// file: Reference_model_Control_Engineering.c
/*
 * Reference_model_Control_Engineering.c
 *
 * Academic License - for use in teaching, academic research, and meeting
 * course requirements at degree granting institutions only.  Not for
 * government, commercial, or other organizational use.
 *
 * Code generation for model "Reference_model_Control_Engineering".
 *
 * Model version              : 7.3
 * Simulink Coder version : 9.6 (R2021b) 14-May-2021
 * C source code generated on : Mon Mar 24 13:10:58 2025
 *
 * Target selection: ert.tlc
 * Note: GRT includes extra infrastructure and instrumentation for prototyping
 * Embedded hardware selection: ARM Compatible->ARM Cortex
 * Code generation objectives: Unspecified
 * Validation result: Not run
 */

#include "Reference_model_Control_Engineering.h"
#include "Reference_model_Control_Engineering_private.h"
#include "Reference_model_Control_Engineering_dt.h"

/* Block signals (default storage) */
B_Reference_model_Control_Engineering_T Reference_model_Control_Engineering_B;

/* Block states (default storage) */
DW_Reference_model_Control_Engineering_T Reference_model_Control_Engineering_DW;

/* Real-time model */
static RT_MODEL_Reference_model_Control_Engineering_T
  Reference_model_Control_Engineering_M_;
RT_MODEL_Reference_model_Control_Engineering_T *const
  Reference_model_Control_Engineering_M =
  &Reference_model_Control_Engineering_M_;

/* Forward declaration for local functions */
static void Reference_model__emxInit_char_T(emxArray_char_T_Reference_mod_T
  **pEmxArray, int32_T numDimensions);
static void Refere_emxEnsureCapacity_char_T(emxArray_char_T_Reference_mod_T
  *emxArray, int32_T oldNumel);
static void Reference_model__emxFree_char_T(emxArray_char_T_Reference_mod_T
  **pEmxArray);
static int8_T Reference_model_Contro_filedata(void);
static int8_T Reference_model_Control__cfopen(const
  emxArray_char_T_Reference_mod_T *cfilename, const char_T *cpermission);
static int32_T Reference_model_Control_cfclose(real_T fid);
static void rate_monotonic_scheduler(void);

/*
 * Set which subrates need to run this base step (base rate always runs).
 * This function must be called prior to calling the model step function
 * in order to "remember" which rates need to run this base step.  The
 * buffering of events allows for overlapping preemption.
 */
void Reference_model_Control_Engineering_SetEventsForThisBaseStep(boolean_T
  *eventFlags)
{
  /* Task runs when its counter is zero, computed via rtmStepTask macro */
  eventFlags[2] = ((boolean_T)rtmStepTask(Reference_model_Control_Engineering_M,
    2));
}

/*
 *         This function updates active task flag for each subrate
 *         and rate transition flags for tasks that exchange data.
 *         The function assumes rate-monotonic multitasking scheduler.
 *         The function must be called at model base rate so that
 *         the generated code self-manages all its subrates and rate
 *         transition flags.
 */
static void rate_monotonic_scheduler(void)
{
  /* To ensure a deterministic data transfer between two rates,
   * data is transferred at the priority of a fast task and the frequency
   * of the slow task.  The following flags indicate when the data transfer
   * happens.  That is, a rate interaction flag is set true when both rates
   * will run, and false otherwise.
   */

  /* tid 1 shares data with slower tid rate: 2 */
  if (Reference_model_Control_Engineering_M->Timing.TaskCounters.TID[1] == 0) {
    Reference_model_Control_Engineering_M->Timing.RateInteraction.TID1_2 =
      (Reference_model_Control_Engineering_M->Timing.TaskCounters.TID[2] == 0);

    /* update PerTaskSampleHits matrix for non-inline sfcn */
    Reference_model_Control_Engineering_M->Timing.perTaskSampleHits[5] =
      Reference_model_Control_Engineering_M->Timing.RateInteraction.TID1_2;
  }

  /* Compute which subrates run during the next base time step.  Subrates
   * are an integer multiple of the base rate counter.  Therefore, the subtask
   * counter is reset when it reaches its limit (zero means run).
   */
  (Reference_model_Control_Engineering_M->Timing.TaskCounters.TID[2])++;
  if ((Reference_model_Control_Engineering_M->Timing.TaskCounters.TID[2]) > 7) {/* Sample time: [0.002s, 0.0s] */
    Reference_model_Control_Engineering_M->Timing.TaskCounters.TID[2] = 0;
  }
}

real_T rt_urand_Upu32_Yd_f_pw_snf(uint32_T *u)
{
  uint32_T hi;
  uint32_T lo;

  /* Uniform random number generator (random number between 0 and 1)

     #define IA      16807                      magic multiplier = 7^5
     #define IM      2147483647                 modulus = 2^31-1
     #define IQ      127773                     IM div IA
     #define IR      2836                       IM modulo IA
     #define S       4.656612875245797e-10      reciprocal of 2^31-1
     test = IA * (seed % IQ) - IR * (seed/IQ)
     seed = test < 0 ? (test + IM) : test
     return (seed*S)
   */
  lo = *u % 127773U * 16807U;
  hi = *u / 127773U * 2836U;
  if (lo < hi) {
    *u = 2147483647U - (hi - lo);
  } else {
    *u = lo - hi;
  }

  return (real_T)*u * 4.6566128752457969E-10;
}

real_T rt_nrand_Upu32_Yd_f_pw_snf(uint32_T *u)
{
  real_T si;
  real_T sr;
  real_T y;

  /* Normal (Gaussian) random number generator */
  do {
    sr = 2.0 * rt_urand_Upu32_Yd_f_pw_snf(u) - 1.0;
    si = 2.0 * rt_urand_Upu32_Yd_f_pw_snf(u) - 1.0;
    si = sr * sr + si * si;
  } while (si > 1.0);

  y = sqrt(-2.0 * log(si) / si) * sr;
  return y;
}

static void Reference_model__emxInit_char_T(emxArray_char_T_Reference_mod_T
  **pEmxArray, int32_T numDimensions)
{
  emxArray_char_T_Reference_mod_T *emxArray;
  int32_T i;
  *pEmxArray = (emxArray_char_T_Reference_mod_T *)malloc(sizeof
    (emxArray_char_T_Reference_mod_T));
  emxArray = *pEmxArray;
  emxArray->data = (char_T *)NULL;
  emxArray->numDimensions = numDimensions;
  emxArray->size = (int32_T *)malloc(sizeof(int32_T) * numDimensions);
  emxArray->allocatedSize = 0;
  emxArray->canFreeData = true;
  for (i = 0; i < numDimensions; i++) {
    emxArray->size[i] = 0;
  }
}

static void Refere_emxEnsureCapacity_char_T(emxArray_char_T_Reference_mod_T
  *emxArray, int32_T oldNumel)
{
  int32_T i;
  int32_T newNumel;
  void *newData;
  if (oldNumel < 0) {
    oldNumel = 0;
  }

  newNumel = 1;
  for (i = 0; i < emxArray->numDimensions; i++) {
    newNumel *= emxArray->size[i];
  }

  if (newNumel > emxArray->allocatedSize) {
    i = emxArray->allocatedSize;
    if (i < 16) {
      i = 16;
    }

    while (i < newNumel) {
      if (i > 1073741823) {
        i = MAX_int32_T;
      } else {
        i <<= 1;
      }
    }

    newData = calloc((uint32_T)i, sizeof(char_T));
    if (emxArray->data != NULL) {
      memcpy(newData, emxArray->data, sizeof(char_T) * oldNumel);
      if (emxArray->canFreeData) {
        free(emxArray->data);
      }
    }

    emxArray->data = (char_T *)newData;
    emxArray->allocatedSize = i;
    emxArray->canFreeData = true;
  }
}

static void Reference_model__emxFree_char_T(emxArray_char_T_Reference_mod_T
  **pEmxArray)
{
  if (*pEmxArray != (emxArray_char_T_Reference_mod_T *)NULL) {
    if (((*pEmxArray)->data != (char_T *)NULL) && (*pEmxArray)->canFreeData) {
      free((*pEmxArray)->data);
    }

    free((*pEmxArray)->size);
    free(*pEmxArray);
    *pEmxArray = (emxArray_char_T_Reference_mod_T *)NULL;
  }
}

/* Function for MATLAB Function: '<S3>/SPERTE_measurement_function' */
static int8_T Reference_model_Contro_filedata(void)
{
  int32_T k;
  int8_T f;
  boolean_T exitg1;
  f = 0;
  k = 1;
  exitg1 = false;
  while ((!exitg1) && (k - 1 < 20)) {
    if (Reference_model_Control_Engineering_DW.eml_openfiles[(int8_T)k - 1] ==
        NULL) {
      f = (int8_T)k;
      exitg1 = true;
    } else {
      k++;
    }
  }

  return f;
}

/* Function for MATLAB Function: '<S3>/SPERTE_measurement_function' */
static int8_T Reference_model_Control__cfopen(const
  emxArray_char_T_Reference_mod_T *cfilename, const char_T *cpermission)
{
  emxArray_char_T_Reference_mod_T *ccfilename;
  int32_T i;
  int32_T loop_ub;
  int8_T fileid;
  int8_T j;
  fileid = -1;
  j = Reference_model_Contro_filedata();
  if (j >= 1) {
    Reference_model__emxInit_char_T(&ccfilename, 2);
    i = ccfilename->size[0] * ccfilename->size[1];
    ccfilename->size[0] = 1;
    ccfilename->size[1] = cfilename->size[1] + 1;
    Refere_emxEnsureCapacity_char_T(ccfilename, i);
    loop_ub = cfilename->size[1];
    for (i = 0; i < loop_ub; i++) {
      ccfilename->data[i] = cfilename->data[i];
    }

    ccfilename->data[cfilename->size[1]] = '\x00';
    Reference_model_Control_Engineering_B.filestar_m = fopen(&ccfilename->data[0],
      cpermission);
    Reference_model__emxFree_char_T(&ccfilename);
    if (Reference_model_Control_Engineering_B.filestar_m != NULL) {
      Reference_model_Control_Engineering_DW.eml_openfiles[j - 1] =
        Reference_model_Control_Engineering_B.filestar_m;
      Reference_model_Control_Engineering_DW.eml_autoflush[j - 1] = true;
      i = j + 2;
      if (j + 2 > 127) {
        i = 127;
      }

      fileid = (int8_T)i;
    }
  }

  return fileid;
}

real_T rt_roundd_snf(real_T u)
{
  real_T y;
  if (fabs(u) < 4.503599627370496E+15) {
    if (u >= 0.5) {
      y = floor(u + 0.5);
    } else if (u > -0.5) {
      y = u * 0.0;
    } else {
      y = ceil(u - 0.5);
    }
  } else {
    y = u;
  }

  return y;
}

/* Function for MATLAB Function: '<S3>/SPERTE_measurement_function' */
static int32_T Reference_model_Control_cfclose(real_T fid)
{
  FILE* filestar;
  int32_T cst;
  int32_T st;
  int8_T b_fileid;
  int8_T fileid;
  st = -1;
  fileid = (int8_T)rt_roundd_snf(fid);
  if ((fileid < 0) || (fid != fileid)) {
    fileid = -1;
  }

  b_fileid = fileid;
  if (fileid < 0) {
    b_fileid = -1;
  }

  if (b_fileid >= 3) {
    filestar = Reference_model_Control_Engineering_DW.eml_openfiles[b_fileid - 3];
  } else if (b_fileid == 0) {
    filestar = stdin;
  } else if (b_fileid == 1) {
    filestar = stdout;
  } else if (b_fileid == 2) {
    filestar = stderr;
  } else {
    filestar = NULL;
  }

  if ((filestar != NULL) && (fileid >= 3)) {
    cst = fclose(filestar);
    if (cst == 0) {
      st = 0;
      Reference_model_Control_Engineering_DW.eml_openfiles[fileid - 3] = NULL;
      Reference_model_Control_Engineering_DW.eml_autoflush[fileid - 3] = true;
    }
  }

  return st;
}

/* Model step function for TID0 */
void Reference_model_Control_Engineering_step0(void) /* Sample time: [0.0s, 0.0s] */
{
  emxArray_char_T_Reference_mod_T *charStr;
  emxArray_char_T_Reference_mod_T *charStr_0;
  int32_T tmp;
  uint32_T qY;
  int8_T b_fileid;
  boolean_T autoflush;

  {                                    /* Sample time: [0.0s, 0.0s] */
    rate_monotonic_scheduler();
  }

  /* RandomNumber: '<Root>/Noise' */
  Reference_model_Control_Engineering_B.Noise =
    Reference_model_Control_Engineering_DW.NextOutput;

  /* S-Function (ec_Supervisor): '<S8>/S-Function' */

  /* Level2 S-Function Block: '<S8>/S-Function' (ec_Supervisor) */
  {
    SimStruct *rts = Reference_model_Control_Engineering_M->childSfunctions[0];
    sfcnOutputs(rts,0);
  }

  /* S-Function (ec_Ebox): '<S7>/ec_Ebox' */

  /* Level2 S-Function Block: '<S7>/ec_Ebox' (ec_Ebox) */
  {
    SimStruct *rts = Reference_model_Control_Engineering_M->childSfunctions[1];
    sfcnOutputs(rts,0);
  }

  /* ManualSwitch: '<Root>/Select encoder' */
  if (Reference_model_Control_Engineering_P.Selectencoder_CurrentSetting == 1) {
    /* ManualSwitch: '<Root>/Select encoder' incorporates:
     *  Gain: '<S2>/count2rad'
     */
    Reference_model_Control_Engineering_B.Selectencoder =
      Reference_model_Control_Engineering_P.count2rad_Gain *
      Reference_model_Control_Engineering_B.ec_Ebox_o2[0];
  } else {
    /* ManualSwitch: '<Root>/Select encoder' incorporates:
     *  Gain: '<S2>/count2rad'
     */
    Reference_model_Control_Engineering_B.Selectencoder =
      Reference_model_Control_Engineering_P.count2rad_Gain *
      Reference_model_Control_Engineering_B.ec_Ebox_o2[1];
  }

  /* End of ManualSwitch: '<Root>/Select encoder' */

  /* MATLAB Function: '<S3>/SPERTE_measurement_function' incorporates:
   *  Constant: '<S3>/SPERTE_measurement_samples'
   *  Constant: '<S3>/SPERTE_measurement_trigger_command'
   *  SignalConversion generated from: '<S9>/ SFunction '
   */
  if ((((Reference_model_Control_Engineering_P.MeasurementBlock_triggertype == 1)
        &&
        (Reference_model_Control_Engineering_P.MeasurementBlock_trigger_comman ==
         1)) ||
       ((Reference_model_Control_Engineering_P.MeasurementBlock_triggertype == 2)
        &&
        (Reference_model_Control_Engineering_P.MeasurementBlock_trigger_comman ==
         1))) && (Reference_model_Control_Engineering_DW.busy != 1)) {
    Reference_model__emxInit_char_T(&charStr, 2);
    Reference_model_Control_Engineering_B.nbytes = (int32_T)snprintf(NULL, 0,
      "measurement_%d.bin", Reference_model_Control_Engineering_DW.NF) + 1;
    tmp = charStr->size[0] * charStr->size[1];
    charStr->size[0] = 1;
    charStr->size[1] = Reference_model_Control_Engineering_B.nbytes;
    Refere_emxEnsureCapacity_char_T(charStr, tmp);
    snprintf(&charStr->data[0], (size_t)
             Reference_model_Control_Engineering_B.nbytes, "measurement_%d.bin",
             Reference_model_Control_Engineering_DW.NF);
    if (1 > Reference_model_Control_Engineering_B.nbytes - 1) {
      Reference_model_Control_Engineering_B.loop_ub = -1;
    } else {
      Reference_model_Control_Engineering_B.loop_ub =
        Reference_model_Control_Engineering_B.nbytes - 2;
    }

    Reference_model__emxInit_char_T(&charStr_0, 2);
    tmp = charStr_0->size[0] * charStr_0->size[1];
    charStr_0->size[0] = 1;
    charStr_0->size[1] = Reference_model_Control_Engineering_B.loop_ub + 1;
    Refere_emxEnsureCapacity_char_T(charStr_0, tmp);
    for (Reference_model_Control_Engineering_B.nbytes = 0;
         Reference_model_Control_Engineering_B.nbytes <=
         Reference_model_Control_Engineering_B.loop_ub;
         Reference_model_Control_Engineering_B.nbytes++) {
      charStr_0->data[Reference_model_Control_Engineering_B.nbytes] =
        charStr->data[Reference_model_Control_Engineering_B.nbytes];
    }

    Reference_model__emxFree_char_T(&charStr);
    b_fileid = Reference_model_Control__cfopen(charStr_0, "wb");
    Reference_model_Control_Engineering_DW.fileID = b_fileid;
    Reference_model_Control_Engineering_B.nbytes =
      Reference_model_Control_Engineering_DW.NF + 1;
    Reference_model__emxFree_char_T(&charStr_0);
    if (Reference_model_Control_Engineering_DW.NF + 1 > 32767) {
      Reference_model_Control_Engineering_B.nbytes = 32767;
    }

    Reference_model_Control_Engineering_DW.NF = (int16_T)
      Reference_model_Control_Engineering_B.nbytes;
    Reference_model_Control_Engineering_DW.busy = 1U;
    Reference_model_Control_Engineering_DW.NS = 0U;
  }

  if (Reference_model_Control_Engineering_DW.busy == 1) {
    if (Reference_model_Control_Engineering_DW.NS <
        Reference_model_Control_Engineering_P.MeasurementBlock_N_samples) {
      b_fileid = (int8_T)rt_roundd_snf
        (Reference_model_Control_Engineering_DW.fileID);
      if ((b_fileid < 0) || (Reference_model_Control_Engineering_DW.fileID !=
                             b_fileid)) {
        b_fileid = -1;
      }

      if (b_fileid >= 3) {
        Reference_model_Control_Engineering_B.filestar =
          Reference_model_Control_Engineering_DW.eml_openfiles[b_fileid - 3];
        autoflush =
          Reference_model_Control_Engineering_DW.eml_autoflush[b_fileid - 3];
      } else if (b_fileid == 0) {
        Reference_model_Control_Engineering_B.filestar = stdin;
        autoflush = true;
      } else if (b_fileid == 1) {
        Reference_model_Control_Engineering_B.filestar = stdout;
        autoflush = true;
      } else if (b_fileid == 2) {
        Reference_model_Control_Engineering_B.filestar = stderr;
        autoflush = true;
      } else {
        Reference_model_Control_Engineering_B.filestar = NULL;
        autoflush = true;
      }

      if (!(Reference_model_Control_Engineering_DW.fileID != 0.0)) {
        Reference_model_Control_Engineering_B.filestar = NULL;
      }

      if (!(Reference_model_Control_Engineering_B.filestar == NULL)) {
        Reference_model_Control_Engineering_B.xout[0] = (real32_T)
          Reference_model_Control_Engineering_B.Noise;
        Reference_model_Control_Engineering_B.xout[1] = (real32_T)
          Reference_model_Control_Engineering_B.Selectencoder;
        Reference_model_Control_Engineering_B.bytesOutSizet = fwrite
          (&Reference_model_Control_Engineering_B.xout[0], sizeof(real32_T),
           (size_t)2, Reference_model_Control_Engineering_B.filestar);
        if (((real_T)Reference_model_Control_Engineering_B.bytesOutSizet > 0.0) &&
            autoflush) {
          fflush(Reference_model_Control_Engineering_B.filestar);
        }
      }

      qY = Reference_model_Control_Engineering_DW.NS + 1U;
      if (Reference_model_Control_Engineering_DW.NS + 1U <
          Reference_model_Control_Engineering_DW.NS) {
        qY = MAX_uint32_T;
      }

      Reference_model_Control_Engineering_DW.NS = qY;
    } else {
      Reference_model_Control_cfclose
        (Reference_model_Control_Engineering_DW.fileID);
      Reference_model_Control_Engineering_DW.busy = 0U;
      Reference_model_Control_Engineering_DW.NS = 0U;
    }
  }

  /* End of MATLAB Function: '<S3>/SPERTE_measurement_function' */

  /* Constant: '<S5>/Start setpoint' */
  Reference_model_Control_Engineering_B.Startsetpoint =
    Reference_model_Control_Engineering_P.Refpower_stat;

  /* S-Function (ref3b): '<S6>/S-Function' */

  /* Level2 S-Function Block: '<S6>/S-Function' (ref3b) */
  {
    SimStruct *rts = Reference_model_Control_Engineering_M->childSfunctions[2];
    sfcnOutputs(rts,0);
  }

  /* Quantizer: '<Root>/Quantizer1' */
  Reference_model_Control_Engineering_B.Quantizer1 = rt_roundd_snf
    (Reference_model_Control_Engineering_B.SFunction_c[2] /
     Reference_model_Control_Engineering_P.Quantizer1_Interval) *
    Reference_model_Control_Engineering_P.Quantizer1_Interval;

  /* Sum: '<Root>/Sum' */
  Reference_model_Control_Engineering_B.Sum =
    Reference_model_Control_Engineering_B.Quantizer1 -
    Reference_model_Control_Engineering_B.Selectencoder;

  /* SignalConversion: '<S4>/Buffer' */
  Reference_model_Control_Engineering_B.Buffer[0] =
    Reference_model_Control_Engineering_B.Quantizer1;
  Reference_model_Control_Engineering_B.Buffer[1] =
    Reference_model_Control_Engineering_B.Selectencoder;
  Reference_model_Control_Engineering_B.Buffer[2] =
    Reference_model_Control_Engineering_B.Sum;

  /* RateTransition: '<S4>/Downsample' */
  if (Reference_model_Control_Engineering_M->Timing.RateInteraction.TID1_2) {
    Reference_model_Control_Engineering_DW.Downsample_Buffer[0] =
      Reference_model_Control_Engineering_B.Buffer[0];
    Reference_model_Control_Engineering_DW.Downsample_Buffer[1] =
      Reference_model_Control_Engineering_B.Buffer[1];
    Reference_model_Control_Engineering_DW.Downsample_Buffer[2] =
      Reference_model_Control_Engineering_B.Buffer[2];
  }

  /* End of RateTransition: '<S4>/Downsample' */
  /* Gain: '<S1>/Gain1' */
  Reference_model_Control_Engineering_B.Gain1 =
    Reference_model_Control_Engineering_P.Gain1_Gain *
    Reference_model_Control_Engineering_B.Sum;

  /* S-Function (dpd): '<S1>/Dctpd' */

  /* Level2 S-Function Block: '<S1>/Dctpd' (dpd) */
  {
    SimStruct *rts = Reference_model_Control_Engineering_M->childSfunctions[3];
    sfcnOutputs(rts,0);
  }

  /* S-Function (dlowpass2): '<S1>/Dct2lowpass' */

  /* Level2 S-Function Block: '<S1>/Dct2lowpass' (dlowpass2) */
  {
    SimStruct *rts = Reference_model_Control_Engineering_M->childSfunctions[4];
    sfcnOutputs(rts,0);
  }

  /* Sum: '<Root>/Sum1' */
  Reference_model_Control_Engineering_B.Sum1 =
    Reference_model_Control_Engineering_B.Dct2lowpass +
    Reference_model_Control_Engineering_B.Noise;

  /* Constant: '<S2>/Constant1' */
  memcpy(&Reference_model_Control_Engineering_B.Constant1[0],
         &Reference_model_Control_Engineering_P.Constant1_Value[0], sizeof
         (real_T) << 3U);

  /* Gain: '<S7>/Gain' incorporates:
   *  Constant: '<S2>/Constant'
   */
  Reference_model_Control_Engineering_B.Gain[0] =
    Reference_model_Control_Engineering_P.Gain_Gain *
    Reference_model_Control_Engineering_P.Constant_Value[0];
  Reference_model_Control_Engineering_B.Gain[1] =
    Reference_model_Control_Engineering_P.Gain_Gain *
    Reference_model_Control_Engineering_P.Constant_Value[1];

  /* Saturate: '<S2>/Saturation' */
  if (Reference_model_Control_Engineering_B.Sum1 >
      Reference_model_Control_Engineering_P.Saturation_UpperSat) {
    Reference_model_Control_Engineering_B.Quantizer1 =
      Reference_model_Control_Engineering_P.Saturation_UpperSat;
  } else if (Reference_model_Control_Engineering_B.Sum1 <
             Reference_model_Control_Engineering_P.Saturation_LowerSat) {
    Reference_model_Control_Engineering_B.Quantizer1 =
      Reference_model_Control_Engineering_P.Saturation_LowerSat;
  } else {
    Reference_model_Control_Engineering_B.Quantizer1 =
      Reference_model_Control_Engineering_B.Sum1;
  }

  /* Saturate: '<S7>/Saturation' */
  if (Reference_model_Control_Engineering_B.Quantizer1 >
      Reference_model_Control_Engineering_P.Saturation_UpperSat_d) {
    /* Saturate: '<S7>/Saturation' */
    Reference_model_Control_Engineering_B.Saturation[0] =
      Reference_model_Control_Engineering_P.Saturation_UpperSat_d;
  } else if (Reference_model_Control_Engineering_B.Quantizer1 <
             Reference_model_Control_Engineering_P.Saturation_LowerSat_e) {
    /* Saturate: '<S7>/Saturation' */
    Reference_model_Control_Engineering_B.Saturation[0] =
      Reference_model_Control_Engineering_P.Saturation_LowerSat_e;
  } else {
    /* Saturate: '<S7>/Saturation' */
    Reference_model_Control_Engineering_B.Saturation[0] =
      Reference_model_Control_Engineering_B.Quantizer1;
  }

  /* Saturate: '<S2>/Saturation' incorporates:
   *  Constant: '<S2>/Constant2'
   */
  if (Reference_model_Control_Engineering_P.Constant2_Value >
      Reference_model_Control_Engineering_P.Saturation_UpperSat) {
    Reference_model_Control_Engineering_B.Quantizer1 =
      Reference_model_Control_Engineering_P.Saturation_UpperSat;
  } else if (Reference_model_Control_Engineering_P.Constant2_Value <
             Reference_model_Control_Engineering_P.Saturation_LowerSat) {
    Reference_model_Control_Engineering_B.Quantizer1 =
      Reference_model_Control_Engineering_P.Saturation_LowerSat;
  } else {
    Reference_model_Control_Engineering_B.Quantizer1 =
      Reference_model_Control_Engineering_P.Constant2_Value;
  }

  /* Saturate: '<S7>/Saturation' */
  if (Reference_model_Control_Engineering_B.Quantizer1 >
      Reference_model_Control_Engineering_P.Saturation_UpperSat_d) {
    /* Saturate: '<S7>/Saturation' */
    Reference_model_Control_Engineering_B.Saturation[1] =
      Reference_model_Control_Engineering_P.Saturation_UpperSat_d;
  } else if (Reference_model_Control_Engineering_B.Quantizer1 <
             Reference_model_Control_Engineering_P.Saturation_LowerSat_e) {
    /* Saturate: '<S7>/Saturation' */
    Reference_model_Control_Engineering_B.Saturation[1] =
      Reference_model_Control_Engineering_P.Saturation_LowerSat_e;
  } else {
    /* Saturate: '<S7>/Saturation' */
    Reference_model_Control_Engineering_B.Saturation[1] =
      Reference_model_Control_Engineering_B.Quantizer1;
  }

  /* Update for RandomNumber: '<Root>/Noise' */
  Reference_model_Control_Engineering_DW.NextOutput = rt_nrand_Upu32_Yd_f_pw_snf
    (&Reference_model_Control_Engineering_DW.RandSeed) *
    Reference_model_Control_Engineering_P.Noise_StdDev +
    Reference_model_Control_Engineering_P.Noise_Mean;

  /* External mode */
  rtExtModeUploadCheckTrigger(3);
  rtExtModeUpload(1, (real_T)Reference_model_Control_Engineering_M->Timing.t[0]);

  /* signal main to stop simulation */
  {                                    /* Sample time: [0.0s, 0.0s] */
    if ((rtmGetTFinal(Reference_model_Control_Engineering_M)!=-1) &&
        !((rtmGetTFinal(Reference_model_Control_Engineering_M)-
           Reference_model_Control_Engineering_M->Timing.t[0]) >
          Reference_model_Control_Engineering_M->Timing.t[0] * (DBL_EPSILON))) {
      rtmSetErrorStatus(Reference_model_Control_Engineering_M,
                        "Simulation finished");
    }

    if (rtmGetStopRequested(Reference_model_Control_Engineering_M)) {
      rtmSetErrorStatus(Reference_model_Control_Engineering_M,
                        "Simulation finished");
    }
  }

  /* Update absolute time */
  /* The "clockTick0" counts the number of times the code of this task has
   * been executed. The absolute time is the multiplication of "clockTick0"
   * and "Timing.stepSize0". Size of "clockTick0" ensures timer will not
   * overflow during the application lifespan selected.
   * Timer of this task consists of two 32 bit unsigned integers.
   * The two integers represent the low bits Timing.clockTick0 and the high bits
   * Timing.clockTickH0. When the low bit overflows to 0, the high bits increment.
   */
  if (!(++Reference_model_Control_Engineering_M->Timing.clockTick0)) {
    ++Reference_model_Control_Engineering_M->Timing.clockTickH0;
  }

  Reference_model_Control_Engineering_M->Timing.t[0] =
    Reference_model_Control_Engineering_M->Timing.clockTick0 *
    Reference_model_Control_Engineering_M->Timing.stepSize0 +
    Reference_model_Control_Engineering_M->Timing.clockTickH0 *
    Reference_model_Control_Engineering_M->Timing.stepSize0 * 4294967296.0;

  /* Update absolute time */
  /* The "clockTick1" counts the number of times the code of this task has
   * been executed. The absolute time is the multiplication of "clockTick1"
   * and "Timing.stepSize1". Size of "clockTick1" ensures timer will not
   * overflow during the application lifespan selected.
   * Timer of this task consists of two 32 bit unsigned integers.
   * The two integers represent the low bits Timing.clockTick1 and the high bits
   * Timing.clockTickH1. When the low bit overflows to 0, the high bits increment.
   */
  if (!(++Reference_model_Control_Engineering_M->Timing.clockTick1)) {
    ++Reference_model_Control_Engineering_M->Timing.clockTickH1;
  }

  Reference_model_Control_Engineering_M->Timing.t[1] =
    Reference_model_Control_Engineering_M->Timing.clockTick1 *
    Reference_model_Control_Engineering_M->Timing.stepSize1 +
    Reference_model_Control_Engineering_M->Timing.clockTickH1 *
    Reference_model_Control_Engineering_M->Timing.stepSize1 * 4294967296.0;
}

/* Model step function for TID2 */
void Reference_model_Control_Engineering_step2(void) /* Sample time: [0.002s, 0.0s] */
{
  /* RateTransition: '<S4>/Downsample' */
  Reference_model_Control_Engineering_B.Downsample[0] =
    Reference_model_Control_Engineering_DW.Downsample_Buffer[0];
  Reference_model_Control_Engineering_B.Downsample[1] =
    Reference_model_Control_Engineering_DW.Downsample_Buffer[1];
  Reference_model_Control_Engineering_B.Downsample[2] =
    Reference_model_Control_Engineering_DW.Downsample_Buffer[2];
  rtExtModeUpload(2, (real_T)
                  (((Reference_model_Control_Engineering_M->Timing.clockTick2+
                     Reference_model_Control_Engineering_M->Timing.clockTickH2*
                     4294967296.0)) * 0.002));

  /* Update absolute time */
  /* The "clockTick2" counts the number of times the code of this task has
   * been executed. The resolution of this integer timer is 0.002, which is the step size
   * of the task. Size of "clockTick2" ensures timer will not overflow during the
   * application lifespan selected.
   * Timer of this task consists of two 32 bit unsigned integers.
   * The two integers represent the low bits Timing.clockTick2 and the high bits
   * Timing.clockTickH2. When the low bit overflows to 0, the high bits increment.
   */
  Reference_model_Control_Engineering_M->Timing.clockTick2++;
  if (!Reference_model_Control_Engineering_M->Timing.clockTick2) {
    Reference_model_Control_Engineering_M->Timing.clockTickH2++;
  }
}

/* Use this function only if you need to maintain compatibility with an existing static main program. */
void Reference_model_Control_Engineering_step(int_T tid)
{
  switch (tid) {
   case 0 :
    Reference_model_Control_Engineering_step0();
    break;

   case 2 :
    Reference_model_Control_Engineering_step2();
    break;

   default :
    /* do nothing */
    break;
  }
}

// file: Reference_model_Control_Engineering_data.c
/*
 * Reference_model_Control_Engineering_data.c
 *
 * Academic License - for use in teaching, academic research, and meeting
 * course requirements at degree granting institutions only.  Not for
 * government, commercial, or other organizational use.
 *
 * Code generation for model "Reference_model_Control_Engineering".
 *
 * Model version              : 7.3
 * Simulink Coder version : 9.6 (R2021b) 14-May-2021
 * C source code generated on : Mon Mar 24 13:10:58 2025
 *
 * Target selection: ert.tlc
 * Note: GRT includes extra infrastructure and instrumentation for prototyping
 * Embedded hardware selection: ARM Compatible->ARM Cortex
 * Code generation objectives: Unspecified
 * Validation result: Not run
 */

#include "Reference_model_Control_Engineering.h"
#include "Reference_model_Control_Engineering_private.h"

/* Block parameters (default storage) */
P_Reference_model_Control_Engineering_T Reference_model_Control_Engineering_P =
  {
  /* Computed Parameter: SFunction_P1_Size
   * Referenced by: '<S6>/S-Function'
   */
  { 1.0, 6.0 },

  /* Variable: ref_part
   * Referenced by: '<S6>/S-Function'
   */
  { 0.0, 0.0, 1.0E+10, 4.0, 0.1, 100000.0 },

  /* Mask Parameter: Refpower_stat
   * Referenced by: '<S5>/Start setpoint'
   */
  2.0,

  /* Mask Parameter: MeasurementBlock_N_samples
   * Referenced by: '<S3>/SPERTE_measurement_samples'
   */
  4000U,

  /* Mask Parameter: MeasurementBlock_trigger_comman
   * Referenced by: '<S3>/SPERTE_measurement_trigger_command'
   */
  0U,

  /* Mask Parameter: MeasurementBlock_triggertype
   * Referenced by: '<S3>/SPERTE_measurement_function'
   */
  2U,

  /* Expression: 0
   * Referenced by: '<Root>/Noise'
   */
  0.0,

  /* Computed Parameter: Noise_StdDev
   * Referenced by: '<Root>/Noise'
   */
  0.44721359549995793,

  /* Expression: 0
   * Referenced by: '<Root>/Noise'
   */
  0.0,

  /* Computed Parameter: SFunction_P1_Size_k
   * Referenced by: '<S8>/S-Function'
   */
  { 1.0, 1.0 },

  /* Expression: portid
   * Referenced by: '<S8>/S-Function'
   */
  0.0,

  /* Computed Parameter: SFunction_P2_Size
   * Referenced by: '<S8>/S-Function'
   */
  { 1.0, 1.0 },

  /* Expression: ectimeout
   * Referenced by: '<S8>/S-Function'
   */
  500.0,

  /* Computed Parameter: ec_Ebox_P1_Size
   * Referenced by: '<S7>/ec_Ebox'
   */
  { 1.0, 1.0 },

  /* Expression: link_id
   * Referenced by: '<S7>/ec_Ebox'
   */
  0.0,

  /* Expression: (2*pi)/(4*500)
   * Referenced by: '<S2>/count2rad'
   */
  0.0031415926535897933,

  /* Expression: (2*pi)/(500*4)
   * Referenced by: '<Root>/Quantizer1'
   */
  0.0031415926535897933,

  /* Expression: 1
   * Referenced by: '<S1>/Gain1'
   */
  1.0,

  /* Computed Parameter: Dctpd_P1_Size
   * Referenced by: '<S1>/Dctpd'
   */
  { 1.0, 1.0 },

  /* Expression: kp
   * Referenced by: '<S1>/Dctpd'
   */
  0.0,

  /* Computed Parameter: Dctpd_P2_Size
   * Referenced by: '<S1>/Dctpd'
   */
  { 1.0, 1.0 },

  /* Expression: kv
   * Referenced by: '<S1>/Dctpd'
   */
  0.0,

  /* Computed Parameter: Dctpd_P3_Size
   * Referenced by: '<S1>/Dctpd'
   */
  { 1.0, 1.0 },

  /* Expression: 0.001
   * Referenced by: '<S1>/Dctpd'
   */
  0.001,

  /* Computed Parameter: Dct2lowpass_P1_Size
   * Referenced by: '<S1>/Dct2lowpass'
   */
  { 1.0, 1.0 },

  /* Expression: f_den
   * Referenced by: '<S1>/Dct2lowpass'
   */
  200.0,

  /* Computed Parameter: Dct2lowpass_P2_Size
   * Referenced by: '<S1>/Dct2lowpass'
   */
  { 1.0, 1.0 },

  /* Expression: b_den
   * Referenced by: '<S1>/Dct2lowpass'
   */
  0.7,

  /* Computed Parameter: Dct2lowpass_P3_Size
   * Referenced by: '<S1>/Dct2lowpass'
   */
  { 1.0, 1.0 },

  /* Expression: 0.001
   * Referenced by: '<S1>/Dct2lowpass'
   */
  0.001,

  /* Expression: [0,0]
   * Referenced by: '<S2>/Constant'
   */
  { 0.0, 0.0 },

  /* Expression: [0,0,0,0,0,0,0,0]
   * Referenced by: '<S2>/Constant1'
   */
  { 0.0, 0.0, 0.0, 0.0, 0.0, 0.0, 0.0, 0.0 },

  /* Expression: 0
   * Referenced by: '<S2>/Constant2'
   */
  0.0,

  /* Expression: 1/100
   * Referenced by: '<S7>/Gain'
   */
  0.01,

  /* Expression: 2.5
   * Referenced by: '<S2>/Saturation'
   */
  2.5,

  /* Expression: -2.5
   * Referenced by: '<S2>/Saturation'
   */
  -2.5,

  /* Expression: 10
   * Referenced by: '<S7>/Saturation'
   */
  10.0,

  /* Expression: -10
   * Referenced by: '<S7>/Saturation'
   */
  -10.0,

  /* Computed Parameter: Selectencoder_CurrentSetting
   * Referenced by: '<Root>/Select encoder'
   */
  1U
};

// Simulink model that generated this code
simulink model "Reference_model_Control_Engineering"  (R2021b)
settings: Solver=FixedStepDiscrete  StartTime=0.0  StopTime=inf  FixedStep=Ts  RelTol=1e-3  EnableMultiTasking=on
InitFcn:
  | Fs = 4000; Ts = 1/Fs; tsim = 29.9997;

== system Reference_model_Control_Engineering ==
  note: Add more signals by expanding the Mux ports
  note: The measurement block is used to obtain high-samplerate measurements
  note: This realtime scope is used to monitor signals
  note: Always accept the reference once before starting the model.
  note: Change the variance of the noise but keep it reasonable <0.5
  Controller (motor side) : Subsystem
  For two point method use this : Mux  Inputs=2
  Fourth Order Motion System : Subsystem
  Measurement Block : Subsystem  Description=|  Priority=-1  mask(SPERTE Lib){N_samples=4000, triggertype=2, trigger_command=0}
      | Perform on-demand measurements to file using this block.
      | 
      | It can be used in 2 ways:
      | 1) Set the mask triggertype parameter to manual and use the trigger input signal to trigger a measurement.
      | You can do this by providing a 0 to 1 transition.
      | Keep it low after you start/complete the measurement, or it will measure again.
      | A file is created with measurement_0,1,2... etc
      | 
      | 2) Keep the model running, and trigger a measurement from the commandline or Matlab script.
      | For example:
      | 
      | % How many samples to measure?
      | N_samples = Fs*5;
      | % Do the measurement
      | SPERTE_Perform_Measurement(N_samples);
      | % Get the latest file
      | file_list = SPERTE_Get_Latest_Measurement(p,1,'./data');
      | % How many signals did you record?
      | N_signals = 3;
      | % Convert the .bin to .mat and return the results
      | measurement = SPERTE_Bin_To_Mat(file_list,N_signals);
      mask prompts: N_samples "Number of samples"; trigger_command "Trigger command"
      mask help:
      | This block implements a measurement to file sink.
      | It can be used in two ways:
      | 1) Triggered from the simulink model
      | 2) Triggered from the command line
  Mux : Mux  Inputs=3
  Mux1 : Mux  Inputs=2
  Noise : RandomNumber  Variance=0.2  SampleTime=Ts
  Quantizer1 : Quantizer  QuantizationInterval=(2*pi)/(500*4)
  Real-time scope : Subsystem  Priority=0  mask(Scope){Sample_Time=1/500}
      mask prompts: Sample_Time "Scope sample time"
      mask help:
      | Realtime Scope block allows one to view the signals while the model is running.
      | The signals are downsampled to a specified sample rate (in the mask parameter) to reduce communication overhead.
  Ref power : Subsystem  mask(On/Off Switch){stat=Off}
      mask prompts: stat "Switch"
  Select encoder : ManualSwitch
  Subsystem : Subsystem  mask(Ref3){}
  Sum : Sum  Inputs=|+-
  Sum1 : Sum  Inputs=|++
  Terminator : Terminator
  Terminator1 : Terminator
  To Workspace : ToWorkspace  VariableName=simout_disturb  SaveFormat=Structure With Time  SampleTime=-1
  To Workspace1 : ToWorkspace  VariableName=simout_u  SaveFormat=Structure With Time  SampleTime=-1
  To Workspace2 : ToWorkspace  VariableName=simout_error  SaveFormat=Structure With Time  SampleTime=-1
  To Workspace3 : ToWorkspace  VariableName=simout_controller  SaveFormat=Structure With Time  SampleTime=-1
  To Workspace4 : ToWorkspace  VariableName=simout_y  SaveFormat=Structure With Time  SampleTime=-1
  wires:
  Fourth Order Motion System/1(Motor [rad]) -> Select encoder/1
  Fourth Order Motion System/2(Load [rad]) -> Select encoder/2
  Select encoder/1 -> Mux/2, Sum/2, Mux1/2, To Workspace4/1
  Sum1/1 -> To Workspace1/1, Fourth Order Motion System/1(Motor [v])
  Controller (motor side)/1(control signal) -> To Workspace3/1, Sum1/1
  Sum/1 -> To Workspace2/1, Controller (motor side)/1(error), Mux/3
  Quantizer1/1 -> Mux/1, Sum/1
  Ref power/1(On/Off) -> Subsystem/1(start)
  Subsystem/3(pos) -> Quantizer1/1
  Mux/1 -> Real-time scope/1(In1)
  Mux1/1 -> Measurement Block/2(Signals)
  Subsystem/1(acc) -> Terminator/1
  Subsystem/2(vel) -> Terminator1/1
  Noise/1 -> To Workspace/1, Sum1/2, Mux1/1

== system Reference_model_Control_Engineering/Controller (motor side) ==
  error : Inport
  Dct2lowpass : S-Function  FunctionName=dlowpass2  Parameters=f_den, b_den, 0.001  SFunctionDeploymentMode=off  EnableBusSupport=off  mask(dctools){f_den=200, b_den=0.7}
      mask prompts: f_den "Pole [Hz]"; b_den "Damping pole [-]"
      mask help: This block implements a discrete time 2nd order lowpass filter.
  Dctpd : S-Function  FunctionName=dpd  Parameters=kp, kv, 0.001  SFunctionDeploymentMode=off  EnableBusSupport=off  mask(dctools){kp=0, kv=0}
      mask help: This block implements a discrete time pd filter.
  Gain1 : Gain  SaturateOnIntegerOverflow=on  OutDataTypeStr=Inherit: Same as input  ParamDataTypeStr=Inherit: Same as input
  control signal : Outport
  wires:
  Dct2lowpass/1 -> control signal/1
  Gain1/1 -> Dctpd/1
  error/1 -> Gain1/1
  Dctpd/1 -> Dct2lowpass/1

== system Reference_model_Control_Engineering/Fourth Order Motion System ==
  Motor [v] : Inport
  Constant : Constant  Value=[0,0]
  Constant1 : Constant  Value=[0,0,0,0,0,0,0,0]
  Constant2 : Constant  Value=0
  Demux : Demux  Outputs=2
  Ethercat E-box : Subsystem  Priority=-2  mask(Sperte Lib){link_id=0}
      mask prompts: link_id "Link ID of the specific ebox"
      mask help:
      | This block implements a single E-box device.
      | Ensure that if you have multiple E-box devices that they each have an unique link_id.
      |
      | You MUST have an Ethercat Initialize block in your model to be able to use this block.
  Ethercat Supervisor : Subsystem  Description=Must be executed first, keep at -1 priority (highest)  Priority=-3  mask(Sperte Lib){portid=0, ectimeout=500}
      mask prompts: portid "Ethernet port number for the Ethercat protocol (default 0 = eth0)"; ectimeout "Timeout of the Ethercat protocol in microseconds."
      mask help:
      | This block initializes the Ethercat connection on the Raspberry Pi.
      |
      | This enables you to use multiple E-box devices by including multiple blocks of the "Ethercat E-box" type.
  Mux : Mux  Inputs=2
  Saturation : Saturate  UpperLimit=2.5  LowerLimit=-2.5
  Terminator : Terminator
  Terminator1 : Terminator
  Terminator2 : Terminator
  count2rad : Gain  Gain=(2*pi)/(4*500)
  Motor [rad] : Outport
  Load [rad] : Outport  Port=2
  wires:
  Ethercat E-box/1(ADC [v]) -> Terminator1/1
  Ethercat E-box/2(ENC [count]) -> count2rad/1
  Constant/1 -> Ethercat E-box/2(PWM [%])
  Mux/1 -> Saturation/1
  count2rad/1 -> Demux/1
  Motor [v]/1 -> Mux/1
  Constant2/1 -> Mux/2
  Demux/1 -> Motor [rad]/1
  Demux/2 -> Load [rad]/1
  Ethercat E-box/3(DI [1/0]) -> Terminator/1
  Constant1/1 -> Ethercat E-box/3(DO [1/0])
  Saturation/1 -> Ethercat E-box/1(DAC [v])
  Ethercat Supervisor/1(Status) -> Terminator2/1

== system Reference_model_Control_Engineering/Measurement Block ==
  Trigger : Inport
  Signals : Inport  Port=2
  SPERTE_measurement_function : MATLAB Function  TreatAsAtomicUnit=on
  SPERTE_measurement_samples : Constant  Value=N_samples  OutDataTypeStr=uint32
  SPERTE_measurement_trigger_command : Constant  Value=trigger_command  OutDataTypeStr=uint8
  Status : Outport
  wires:
  SPERTE_measurement_samples/1 -> SPERTE_measurement_function/4(N_samples)
  SPERTE_measurement_trigger_command/1 -> SPERTE_measurement_function/3(trigger_command)
  Signals/1 -> SPERTE_measurement_function/1(u)
  Trigger/1 -> SPERTE_measurement_function/2(trigger_manual)
  SPERTE_measurement_function/1(status) -> Status/1

== system Reference_model_Control_Engineering/Real-time scope ==
  note: The default scope sample rate is 500 Hz.
      | This can be changed by right-click on the Realtime Scope block.
      | Then selecting -> Mask -> Mask parameters.
  In1 : Inport
  Buffer : SignalConversion  OverrideOpt=off
  Downsample : RateTransition  OutPortSampleTime=Sample_Time
  Live_Scope : Scope
  wires:
  In1/1 -> Buffer/1
  Downsample/1 -> Live_Scope/1
  Buffer/1 -> Downsample/1

== system Reference_model_Control_Engineering/Ref power ==
  Start setpoint : Constant  Value=stat
  On/Off : Outport
  wires:
  Start setpoint/1 -> On/Off/1

== system Reference_model_Control_Engineering/Subsystem ==
  start : Inport
  Demux : Demux  Outputs=3
  S-Function : S-Function  FunctionName=ref3b  Parameters=ref_part  SFunctionDeploymentMode=off  EnableBusSupport=off
  acc : Outport
  vel : Outport  Port=2
  pos : Outport  Port=3
  wires:
  S-Function/1 -> Demux/1
  Demux/1 -> acc/1
  Demux/2 -> vel/1
  Demux/3 -> pos/1
  start/1 -> S-Function/1

== system Reference_model_Control_Engineering/Fourth Order Motion System/Ethercat E-box ==
  DAC [v] : Inport
  PWM [%] : Inport  Port=2
  DO [1/0] : Inport  Port=3
  Gain : Gain  Gain=1/100
  Saturation : Saturate  UpperLimit=10  LowerLimit=-10
  ec_Ebox : S-Function  FunctionName=ec_Ebox  Parameters=link_id  SFunctionDeploymentMode=off  EnableBusSupport=off  mask{link_id=link_id}
      mask prompts: link_id "link_id >= 0"
  ADC [v] : Outport
  ENC [count] : Outport  Port=2
  DI [1/0] : Outport  Port=3
  wires:
  Gain/1 -> ec_Ebox/2
  Saturation/1 -> ec_Ebox/1
  ec_Ebox/3 -> DI [1/0]/1
  ec_Ebox/1 -> ADC [v]/1
  ec_Ebox/2 -> ENC [count]/1
  DAC [v]/1 -> Saturation/1
  DO [1/0]/1 -> ec_Ebox/3
  PWM [%]/1 -> Gain/1

== system Reference_model_Control_Engineering/Fourth Order Motion System/Ethercat Supervisor ==
  note: Status, 0 = Operational, 1 = error
  S-Function : S-Function  FunctionName=ec_Supervisor  Parameters=portid,ectimeout  SFunctionDeploymentMode=off  EnableBusSupport=off
  Status : Outport
  wires:
  S-Function/1 -> Status/1

== matlab function Reference_model_Control_Engineering/Measurement Block/SPERTE_measurement_function ==
function status = perform_measurement(u, trigger_manual, trigger_command, triggertype, N_samples)

%% Persistent variables
persistent fileID NF busy NS

% Init parameters
if isempty(NF)
    NF = int16(0);
end
if isempty(NS)
    NS = uint32(0);
end
if isempty(fileID)
    fileID = 0;
end
if isempty(busy)
    busy = uint8(0);
end

%% Check the triggers
if ( (triggertype == 0 && trigger_manual == 1) || (triggertype == 1 && trigger_command == 1) || (triggertype == 2 && (trigger_command == 1 || trigger_manual == 1) ) )
    if busy == 1
        % We are already busy, nothing to do
    else
        % We should start a new one
        fileID = fopen(sprintf('measurement_%d.bin',NF),'w');  
        NF = NF + 1;
        busy = uint8(1);
        NS = uint32(0);
    end
end

% We have started a measurement
if busy == 1
    if NS < N_samples 
        % Here we write the sample, in single precision float
        fwrite(fileID,u,'single');
        NS = NS + uint32(1);
    else
       % We have N samples already, we are done
       fclose(fileID);
       busy = uint8(0);
       NS = uint32(0);
    end
      
end
    % Output state
    status = uint8(busy);
end
